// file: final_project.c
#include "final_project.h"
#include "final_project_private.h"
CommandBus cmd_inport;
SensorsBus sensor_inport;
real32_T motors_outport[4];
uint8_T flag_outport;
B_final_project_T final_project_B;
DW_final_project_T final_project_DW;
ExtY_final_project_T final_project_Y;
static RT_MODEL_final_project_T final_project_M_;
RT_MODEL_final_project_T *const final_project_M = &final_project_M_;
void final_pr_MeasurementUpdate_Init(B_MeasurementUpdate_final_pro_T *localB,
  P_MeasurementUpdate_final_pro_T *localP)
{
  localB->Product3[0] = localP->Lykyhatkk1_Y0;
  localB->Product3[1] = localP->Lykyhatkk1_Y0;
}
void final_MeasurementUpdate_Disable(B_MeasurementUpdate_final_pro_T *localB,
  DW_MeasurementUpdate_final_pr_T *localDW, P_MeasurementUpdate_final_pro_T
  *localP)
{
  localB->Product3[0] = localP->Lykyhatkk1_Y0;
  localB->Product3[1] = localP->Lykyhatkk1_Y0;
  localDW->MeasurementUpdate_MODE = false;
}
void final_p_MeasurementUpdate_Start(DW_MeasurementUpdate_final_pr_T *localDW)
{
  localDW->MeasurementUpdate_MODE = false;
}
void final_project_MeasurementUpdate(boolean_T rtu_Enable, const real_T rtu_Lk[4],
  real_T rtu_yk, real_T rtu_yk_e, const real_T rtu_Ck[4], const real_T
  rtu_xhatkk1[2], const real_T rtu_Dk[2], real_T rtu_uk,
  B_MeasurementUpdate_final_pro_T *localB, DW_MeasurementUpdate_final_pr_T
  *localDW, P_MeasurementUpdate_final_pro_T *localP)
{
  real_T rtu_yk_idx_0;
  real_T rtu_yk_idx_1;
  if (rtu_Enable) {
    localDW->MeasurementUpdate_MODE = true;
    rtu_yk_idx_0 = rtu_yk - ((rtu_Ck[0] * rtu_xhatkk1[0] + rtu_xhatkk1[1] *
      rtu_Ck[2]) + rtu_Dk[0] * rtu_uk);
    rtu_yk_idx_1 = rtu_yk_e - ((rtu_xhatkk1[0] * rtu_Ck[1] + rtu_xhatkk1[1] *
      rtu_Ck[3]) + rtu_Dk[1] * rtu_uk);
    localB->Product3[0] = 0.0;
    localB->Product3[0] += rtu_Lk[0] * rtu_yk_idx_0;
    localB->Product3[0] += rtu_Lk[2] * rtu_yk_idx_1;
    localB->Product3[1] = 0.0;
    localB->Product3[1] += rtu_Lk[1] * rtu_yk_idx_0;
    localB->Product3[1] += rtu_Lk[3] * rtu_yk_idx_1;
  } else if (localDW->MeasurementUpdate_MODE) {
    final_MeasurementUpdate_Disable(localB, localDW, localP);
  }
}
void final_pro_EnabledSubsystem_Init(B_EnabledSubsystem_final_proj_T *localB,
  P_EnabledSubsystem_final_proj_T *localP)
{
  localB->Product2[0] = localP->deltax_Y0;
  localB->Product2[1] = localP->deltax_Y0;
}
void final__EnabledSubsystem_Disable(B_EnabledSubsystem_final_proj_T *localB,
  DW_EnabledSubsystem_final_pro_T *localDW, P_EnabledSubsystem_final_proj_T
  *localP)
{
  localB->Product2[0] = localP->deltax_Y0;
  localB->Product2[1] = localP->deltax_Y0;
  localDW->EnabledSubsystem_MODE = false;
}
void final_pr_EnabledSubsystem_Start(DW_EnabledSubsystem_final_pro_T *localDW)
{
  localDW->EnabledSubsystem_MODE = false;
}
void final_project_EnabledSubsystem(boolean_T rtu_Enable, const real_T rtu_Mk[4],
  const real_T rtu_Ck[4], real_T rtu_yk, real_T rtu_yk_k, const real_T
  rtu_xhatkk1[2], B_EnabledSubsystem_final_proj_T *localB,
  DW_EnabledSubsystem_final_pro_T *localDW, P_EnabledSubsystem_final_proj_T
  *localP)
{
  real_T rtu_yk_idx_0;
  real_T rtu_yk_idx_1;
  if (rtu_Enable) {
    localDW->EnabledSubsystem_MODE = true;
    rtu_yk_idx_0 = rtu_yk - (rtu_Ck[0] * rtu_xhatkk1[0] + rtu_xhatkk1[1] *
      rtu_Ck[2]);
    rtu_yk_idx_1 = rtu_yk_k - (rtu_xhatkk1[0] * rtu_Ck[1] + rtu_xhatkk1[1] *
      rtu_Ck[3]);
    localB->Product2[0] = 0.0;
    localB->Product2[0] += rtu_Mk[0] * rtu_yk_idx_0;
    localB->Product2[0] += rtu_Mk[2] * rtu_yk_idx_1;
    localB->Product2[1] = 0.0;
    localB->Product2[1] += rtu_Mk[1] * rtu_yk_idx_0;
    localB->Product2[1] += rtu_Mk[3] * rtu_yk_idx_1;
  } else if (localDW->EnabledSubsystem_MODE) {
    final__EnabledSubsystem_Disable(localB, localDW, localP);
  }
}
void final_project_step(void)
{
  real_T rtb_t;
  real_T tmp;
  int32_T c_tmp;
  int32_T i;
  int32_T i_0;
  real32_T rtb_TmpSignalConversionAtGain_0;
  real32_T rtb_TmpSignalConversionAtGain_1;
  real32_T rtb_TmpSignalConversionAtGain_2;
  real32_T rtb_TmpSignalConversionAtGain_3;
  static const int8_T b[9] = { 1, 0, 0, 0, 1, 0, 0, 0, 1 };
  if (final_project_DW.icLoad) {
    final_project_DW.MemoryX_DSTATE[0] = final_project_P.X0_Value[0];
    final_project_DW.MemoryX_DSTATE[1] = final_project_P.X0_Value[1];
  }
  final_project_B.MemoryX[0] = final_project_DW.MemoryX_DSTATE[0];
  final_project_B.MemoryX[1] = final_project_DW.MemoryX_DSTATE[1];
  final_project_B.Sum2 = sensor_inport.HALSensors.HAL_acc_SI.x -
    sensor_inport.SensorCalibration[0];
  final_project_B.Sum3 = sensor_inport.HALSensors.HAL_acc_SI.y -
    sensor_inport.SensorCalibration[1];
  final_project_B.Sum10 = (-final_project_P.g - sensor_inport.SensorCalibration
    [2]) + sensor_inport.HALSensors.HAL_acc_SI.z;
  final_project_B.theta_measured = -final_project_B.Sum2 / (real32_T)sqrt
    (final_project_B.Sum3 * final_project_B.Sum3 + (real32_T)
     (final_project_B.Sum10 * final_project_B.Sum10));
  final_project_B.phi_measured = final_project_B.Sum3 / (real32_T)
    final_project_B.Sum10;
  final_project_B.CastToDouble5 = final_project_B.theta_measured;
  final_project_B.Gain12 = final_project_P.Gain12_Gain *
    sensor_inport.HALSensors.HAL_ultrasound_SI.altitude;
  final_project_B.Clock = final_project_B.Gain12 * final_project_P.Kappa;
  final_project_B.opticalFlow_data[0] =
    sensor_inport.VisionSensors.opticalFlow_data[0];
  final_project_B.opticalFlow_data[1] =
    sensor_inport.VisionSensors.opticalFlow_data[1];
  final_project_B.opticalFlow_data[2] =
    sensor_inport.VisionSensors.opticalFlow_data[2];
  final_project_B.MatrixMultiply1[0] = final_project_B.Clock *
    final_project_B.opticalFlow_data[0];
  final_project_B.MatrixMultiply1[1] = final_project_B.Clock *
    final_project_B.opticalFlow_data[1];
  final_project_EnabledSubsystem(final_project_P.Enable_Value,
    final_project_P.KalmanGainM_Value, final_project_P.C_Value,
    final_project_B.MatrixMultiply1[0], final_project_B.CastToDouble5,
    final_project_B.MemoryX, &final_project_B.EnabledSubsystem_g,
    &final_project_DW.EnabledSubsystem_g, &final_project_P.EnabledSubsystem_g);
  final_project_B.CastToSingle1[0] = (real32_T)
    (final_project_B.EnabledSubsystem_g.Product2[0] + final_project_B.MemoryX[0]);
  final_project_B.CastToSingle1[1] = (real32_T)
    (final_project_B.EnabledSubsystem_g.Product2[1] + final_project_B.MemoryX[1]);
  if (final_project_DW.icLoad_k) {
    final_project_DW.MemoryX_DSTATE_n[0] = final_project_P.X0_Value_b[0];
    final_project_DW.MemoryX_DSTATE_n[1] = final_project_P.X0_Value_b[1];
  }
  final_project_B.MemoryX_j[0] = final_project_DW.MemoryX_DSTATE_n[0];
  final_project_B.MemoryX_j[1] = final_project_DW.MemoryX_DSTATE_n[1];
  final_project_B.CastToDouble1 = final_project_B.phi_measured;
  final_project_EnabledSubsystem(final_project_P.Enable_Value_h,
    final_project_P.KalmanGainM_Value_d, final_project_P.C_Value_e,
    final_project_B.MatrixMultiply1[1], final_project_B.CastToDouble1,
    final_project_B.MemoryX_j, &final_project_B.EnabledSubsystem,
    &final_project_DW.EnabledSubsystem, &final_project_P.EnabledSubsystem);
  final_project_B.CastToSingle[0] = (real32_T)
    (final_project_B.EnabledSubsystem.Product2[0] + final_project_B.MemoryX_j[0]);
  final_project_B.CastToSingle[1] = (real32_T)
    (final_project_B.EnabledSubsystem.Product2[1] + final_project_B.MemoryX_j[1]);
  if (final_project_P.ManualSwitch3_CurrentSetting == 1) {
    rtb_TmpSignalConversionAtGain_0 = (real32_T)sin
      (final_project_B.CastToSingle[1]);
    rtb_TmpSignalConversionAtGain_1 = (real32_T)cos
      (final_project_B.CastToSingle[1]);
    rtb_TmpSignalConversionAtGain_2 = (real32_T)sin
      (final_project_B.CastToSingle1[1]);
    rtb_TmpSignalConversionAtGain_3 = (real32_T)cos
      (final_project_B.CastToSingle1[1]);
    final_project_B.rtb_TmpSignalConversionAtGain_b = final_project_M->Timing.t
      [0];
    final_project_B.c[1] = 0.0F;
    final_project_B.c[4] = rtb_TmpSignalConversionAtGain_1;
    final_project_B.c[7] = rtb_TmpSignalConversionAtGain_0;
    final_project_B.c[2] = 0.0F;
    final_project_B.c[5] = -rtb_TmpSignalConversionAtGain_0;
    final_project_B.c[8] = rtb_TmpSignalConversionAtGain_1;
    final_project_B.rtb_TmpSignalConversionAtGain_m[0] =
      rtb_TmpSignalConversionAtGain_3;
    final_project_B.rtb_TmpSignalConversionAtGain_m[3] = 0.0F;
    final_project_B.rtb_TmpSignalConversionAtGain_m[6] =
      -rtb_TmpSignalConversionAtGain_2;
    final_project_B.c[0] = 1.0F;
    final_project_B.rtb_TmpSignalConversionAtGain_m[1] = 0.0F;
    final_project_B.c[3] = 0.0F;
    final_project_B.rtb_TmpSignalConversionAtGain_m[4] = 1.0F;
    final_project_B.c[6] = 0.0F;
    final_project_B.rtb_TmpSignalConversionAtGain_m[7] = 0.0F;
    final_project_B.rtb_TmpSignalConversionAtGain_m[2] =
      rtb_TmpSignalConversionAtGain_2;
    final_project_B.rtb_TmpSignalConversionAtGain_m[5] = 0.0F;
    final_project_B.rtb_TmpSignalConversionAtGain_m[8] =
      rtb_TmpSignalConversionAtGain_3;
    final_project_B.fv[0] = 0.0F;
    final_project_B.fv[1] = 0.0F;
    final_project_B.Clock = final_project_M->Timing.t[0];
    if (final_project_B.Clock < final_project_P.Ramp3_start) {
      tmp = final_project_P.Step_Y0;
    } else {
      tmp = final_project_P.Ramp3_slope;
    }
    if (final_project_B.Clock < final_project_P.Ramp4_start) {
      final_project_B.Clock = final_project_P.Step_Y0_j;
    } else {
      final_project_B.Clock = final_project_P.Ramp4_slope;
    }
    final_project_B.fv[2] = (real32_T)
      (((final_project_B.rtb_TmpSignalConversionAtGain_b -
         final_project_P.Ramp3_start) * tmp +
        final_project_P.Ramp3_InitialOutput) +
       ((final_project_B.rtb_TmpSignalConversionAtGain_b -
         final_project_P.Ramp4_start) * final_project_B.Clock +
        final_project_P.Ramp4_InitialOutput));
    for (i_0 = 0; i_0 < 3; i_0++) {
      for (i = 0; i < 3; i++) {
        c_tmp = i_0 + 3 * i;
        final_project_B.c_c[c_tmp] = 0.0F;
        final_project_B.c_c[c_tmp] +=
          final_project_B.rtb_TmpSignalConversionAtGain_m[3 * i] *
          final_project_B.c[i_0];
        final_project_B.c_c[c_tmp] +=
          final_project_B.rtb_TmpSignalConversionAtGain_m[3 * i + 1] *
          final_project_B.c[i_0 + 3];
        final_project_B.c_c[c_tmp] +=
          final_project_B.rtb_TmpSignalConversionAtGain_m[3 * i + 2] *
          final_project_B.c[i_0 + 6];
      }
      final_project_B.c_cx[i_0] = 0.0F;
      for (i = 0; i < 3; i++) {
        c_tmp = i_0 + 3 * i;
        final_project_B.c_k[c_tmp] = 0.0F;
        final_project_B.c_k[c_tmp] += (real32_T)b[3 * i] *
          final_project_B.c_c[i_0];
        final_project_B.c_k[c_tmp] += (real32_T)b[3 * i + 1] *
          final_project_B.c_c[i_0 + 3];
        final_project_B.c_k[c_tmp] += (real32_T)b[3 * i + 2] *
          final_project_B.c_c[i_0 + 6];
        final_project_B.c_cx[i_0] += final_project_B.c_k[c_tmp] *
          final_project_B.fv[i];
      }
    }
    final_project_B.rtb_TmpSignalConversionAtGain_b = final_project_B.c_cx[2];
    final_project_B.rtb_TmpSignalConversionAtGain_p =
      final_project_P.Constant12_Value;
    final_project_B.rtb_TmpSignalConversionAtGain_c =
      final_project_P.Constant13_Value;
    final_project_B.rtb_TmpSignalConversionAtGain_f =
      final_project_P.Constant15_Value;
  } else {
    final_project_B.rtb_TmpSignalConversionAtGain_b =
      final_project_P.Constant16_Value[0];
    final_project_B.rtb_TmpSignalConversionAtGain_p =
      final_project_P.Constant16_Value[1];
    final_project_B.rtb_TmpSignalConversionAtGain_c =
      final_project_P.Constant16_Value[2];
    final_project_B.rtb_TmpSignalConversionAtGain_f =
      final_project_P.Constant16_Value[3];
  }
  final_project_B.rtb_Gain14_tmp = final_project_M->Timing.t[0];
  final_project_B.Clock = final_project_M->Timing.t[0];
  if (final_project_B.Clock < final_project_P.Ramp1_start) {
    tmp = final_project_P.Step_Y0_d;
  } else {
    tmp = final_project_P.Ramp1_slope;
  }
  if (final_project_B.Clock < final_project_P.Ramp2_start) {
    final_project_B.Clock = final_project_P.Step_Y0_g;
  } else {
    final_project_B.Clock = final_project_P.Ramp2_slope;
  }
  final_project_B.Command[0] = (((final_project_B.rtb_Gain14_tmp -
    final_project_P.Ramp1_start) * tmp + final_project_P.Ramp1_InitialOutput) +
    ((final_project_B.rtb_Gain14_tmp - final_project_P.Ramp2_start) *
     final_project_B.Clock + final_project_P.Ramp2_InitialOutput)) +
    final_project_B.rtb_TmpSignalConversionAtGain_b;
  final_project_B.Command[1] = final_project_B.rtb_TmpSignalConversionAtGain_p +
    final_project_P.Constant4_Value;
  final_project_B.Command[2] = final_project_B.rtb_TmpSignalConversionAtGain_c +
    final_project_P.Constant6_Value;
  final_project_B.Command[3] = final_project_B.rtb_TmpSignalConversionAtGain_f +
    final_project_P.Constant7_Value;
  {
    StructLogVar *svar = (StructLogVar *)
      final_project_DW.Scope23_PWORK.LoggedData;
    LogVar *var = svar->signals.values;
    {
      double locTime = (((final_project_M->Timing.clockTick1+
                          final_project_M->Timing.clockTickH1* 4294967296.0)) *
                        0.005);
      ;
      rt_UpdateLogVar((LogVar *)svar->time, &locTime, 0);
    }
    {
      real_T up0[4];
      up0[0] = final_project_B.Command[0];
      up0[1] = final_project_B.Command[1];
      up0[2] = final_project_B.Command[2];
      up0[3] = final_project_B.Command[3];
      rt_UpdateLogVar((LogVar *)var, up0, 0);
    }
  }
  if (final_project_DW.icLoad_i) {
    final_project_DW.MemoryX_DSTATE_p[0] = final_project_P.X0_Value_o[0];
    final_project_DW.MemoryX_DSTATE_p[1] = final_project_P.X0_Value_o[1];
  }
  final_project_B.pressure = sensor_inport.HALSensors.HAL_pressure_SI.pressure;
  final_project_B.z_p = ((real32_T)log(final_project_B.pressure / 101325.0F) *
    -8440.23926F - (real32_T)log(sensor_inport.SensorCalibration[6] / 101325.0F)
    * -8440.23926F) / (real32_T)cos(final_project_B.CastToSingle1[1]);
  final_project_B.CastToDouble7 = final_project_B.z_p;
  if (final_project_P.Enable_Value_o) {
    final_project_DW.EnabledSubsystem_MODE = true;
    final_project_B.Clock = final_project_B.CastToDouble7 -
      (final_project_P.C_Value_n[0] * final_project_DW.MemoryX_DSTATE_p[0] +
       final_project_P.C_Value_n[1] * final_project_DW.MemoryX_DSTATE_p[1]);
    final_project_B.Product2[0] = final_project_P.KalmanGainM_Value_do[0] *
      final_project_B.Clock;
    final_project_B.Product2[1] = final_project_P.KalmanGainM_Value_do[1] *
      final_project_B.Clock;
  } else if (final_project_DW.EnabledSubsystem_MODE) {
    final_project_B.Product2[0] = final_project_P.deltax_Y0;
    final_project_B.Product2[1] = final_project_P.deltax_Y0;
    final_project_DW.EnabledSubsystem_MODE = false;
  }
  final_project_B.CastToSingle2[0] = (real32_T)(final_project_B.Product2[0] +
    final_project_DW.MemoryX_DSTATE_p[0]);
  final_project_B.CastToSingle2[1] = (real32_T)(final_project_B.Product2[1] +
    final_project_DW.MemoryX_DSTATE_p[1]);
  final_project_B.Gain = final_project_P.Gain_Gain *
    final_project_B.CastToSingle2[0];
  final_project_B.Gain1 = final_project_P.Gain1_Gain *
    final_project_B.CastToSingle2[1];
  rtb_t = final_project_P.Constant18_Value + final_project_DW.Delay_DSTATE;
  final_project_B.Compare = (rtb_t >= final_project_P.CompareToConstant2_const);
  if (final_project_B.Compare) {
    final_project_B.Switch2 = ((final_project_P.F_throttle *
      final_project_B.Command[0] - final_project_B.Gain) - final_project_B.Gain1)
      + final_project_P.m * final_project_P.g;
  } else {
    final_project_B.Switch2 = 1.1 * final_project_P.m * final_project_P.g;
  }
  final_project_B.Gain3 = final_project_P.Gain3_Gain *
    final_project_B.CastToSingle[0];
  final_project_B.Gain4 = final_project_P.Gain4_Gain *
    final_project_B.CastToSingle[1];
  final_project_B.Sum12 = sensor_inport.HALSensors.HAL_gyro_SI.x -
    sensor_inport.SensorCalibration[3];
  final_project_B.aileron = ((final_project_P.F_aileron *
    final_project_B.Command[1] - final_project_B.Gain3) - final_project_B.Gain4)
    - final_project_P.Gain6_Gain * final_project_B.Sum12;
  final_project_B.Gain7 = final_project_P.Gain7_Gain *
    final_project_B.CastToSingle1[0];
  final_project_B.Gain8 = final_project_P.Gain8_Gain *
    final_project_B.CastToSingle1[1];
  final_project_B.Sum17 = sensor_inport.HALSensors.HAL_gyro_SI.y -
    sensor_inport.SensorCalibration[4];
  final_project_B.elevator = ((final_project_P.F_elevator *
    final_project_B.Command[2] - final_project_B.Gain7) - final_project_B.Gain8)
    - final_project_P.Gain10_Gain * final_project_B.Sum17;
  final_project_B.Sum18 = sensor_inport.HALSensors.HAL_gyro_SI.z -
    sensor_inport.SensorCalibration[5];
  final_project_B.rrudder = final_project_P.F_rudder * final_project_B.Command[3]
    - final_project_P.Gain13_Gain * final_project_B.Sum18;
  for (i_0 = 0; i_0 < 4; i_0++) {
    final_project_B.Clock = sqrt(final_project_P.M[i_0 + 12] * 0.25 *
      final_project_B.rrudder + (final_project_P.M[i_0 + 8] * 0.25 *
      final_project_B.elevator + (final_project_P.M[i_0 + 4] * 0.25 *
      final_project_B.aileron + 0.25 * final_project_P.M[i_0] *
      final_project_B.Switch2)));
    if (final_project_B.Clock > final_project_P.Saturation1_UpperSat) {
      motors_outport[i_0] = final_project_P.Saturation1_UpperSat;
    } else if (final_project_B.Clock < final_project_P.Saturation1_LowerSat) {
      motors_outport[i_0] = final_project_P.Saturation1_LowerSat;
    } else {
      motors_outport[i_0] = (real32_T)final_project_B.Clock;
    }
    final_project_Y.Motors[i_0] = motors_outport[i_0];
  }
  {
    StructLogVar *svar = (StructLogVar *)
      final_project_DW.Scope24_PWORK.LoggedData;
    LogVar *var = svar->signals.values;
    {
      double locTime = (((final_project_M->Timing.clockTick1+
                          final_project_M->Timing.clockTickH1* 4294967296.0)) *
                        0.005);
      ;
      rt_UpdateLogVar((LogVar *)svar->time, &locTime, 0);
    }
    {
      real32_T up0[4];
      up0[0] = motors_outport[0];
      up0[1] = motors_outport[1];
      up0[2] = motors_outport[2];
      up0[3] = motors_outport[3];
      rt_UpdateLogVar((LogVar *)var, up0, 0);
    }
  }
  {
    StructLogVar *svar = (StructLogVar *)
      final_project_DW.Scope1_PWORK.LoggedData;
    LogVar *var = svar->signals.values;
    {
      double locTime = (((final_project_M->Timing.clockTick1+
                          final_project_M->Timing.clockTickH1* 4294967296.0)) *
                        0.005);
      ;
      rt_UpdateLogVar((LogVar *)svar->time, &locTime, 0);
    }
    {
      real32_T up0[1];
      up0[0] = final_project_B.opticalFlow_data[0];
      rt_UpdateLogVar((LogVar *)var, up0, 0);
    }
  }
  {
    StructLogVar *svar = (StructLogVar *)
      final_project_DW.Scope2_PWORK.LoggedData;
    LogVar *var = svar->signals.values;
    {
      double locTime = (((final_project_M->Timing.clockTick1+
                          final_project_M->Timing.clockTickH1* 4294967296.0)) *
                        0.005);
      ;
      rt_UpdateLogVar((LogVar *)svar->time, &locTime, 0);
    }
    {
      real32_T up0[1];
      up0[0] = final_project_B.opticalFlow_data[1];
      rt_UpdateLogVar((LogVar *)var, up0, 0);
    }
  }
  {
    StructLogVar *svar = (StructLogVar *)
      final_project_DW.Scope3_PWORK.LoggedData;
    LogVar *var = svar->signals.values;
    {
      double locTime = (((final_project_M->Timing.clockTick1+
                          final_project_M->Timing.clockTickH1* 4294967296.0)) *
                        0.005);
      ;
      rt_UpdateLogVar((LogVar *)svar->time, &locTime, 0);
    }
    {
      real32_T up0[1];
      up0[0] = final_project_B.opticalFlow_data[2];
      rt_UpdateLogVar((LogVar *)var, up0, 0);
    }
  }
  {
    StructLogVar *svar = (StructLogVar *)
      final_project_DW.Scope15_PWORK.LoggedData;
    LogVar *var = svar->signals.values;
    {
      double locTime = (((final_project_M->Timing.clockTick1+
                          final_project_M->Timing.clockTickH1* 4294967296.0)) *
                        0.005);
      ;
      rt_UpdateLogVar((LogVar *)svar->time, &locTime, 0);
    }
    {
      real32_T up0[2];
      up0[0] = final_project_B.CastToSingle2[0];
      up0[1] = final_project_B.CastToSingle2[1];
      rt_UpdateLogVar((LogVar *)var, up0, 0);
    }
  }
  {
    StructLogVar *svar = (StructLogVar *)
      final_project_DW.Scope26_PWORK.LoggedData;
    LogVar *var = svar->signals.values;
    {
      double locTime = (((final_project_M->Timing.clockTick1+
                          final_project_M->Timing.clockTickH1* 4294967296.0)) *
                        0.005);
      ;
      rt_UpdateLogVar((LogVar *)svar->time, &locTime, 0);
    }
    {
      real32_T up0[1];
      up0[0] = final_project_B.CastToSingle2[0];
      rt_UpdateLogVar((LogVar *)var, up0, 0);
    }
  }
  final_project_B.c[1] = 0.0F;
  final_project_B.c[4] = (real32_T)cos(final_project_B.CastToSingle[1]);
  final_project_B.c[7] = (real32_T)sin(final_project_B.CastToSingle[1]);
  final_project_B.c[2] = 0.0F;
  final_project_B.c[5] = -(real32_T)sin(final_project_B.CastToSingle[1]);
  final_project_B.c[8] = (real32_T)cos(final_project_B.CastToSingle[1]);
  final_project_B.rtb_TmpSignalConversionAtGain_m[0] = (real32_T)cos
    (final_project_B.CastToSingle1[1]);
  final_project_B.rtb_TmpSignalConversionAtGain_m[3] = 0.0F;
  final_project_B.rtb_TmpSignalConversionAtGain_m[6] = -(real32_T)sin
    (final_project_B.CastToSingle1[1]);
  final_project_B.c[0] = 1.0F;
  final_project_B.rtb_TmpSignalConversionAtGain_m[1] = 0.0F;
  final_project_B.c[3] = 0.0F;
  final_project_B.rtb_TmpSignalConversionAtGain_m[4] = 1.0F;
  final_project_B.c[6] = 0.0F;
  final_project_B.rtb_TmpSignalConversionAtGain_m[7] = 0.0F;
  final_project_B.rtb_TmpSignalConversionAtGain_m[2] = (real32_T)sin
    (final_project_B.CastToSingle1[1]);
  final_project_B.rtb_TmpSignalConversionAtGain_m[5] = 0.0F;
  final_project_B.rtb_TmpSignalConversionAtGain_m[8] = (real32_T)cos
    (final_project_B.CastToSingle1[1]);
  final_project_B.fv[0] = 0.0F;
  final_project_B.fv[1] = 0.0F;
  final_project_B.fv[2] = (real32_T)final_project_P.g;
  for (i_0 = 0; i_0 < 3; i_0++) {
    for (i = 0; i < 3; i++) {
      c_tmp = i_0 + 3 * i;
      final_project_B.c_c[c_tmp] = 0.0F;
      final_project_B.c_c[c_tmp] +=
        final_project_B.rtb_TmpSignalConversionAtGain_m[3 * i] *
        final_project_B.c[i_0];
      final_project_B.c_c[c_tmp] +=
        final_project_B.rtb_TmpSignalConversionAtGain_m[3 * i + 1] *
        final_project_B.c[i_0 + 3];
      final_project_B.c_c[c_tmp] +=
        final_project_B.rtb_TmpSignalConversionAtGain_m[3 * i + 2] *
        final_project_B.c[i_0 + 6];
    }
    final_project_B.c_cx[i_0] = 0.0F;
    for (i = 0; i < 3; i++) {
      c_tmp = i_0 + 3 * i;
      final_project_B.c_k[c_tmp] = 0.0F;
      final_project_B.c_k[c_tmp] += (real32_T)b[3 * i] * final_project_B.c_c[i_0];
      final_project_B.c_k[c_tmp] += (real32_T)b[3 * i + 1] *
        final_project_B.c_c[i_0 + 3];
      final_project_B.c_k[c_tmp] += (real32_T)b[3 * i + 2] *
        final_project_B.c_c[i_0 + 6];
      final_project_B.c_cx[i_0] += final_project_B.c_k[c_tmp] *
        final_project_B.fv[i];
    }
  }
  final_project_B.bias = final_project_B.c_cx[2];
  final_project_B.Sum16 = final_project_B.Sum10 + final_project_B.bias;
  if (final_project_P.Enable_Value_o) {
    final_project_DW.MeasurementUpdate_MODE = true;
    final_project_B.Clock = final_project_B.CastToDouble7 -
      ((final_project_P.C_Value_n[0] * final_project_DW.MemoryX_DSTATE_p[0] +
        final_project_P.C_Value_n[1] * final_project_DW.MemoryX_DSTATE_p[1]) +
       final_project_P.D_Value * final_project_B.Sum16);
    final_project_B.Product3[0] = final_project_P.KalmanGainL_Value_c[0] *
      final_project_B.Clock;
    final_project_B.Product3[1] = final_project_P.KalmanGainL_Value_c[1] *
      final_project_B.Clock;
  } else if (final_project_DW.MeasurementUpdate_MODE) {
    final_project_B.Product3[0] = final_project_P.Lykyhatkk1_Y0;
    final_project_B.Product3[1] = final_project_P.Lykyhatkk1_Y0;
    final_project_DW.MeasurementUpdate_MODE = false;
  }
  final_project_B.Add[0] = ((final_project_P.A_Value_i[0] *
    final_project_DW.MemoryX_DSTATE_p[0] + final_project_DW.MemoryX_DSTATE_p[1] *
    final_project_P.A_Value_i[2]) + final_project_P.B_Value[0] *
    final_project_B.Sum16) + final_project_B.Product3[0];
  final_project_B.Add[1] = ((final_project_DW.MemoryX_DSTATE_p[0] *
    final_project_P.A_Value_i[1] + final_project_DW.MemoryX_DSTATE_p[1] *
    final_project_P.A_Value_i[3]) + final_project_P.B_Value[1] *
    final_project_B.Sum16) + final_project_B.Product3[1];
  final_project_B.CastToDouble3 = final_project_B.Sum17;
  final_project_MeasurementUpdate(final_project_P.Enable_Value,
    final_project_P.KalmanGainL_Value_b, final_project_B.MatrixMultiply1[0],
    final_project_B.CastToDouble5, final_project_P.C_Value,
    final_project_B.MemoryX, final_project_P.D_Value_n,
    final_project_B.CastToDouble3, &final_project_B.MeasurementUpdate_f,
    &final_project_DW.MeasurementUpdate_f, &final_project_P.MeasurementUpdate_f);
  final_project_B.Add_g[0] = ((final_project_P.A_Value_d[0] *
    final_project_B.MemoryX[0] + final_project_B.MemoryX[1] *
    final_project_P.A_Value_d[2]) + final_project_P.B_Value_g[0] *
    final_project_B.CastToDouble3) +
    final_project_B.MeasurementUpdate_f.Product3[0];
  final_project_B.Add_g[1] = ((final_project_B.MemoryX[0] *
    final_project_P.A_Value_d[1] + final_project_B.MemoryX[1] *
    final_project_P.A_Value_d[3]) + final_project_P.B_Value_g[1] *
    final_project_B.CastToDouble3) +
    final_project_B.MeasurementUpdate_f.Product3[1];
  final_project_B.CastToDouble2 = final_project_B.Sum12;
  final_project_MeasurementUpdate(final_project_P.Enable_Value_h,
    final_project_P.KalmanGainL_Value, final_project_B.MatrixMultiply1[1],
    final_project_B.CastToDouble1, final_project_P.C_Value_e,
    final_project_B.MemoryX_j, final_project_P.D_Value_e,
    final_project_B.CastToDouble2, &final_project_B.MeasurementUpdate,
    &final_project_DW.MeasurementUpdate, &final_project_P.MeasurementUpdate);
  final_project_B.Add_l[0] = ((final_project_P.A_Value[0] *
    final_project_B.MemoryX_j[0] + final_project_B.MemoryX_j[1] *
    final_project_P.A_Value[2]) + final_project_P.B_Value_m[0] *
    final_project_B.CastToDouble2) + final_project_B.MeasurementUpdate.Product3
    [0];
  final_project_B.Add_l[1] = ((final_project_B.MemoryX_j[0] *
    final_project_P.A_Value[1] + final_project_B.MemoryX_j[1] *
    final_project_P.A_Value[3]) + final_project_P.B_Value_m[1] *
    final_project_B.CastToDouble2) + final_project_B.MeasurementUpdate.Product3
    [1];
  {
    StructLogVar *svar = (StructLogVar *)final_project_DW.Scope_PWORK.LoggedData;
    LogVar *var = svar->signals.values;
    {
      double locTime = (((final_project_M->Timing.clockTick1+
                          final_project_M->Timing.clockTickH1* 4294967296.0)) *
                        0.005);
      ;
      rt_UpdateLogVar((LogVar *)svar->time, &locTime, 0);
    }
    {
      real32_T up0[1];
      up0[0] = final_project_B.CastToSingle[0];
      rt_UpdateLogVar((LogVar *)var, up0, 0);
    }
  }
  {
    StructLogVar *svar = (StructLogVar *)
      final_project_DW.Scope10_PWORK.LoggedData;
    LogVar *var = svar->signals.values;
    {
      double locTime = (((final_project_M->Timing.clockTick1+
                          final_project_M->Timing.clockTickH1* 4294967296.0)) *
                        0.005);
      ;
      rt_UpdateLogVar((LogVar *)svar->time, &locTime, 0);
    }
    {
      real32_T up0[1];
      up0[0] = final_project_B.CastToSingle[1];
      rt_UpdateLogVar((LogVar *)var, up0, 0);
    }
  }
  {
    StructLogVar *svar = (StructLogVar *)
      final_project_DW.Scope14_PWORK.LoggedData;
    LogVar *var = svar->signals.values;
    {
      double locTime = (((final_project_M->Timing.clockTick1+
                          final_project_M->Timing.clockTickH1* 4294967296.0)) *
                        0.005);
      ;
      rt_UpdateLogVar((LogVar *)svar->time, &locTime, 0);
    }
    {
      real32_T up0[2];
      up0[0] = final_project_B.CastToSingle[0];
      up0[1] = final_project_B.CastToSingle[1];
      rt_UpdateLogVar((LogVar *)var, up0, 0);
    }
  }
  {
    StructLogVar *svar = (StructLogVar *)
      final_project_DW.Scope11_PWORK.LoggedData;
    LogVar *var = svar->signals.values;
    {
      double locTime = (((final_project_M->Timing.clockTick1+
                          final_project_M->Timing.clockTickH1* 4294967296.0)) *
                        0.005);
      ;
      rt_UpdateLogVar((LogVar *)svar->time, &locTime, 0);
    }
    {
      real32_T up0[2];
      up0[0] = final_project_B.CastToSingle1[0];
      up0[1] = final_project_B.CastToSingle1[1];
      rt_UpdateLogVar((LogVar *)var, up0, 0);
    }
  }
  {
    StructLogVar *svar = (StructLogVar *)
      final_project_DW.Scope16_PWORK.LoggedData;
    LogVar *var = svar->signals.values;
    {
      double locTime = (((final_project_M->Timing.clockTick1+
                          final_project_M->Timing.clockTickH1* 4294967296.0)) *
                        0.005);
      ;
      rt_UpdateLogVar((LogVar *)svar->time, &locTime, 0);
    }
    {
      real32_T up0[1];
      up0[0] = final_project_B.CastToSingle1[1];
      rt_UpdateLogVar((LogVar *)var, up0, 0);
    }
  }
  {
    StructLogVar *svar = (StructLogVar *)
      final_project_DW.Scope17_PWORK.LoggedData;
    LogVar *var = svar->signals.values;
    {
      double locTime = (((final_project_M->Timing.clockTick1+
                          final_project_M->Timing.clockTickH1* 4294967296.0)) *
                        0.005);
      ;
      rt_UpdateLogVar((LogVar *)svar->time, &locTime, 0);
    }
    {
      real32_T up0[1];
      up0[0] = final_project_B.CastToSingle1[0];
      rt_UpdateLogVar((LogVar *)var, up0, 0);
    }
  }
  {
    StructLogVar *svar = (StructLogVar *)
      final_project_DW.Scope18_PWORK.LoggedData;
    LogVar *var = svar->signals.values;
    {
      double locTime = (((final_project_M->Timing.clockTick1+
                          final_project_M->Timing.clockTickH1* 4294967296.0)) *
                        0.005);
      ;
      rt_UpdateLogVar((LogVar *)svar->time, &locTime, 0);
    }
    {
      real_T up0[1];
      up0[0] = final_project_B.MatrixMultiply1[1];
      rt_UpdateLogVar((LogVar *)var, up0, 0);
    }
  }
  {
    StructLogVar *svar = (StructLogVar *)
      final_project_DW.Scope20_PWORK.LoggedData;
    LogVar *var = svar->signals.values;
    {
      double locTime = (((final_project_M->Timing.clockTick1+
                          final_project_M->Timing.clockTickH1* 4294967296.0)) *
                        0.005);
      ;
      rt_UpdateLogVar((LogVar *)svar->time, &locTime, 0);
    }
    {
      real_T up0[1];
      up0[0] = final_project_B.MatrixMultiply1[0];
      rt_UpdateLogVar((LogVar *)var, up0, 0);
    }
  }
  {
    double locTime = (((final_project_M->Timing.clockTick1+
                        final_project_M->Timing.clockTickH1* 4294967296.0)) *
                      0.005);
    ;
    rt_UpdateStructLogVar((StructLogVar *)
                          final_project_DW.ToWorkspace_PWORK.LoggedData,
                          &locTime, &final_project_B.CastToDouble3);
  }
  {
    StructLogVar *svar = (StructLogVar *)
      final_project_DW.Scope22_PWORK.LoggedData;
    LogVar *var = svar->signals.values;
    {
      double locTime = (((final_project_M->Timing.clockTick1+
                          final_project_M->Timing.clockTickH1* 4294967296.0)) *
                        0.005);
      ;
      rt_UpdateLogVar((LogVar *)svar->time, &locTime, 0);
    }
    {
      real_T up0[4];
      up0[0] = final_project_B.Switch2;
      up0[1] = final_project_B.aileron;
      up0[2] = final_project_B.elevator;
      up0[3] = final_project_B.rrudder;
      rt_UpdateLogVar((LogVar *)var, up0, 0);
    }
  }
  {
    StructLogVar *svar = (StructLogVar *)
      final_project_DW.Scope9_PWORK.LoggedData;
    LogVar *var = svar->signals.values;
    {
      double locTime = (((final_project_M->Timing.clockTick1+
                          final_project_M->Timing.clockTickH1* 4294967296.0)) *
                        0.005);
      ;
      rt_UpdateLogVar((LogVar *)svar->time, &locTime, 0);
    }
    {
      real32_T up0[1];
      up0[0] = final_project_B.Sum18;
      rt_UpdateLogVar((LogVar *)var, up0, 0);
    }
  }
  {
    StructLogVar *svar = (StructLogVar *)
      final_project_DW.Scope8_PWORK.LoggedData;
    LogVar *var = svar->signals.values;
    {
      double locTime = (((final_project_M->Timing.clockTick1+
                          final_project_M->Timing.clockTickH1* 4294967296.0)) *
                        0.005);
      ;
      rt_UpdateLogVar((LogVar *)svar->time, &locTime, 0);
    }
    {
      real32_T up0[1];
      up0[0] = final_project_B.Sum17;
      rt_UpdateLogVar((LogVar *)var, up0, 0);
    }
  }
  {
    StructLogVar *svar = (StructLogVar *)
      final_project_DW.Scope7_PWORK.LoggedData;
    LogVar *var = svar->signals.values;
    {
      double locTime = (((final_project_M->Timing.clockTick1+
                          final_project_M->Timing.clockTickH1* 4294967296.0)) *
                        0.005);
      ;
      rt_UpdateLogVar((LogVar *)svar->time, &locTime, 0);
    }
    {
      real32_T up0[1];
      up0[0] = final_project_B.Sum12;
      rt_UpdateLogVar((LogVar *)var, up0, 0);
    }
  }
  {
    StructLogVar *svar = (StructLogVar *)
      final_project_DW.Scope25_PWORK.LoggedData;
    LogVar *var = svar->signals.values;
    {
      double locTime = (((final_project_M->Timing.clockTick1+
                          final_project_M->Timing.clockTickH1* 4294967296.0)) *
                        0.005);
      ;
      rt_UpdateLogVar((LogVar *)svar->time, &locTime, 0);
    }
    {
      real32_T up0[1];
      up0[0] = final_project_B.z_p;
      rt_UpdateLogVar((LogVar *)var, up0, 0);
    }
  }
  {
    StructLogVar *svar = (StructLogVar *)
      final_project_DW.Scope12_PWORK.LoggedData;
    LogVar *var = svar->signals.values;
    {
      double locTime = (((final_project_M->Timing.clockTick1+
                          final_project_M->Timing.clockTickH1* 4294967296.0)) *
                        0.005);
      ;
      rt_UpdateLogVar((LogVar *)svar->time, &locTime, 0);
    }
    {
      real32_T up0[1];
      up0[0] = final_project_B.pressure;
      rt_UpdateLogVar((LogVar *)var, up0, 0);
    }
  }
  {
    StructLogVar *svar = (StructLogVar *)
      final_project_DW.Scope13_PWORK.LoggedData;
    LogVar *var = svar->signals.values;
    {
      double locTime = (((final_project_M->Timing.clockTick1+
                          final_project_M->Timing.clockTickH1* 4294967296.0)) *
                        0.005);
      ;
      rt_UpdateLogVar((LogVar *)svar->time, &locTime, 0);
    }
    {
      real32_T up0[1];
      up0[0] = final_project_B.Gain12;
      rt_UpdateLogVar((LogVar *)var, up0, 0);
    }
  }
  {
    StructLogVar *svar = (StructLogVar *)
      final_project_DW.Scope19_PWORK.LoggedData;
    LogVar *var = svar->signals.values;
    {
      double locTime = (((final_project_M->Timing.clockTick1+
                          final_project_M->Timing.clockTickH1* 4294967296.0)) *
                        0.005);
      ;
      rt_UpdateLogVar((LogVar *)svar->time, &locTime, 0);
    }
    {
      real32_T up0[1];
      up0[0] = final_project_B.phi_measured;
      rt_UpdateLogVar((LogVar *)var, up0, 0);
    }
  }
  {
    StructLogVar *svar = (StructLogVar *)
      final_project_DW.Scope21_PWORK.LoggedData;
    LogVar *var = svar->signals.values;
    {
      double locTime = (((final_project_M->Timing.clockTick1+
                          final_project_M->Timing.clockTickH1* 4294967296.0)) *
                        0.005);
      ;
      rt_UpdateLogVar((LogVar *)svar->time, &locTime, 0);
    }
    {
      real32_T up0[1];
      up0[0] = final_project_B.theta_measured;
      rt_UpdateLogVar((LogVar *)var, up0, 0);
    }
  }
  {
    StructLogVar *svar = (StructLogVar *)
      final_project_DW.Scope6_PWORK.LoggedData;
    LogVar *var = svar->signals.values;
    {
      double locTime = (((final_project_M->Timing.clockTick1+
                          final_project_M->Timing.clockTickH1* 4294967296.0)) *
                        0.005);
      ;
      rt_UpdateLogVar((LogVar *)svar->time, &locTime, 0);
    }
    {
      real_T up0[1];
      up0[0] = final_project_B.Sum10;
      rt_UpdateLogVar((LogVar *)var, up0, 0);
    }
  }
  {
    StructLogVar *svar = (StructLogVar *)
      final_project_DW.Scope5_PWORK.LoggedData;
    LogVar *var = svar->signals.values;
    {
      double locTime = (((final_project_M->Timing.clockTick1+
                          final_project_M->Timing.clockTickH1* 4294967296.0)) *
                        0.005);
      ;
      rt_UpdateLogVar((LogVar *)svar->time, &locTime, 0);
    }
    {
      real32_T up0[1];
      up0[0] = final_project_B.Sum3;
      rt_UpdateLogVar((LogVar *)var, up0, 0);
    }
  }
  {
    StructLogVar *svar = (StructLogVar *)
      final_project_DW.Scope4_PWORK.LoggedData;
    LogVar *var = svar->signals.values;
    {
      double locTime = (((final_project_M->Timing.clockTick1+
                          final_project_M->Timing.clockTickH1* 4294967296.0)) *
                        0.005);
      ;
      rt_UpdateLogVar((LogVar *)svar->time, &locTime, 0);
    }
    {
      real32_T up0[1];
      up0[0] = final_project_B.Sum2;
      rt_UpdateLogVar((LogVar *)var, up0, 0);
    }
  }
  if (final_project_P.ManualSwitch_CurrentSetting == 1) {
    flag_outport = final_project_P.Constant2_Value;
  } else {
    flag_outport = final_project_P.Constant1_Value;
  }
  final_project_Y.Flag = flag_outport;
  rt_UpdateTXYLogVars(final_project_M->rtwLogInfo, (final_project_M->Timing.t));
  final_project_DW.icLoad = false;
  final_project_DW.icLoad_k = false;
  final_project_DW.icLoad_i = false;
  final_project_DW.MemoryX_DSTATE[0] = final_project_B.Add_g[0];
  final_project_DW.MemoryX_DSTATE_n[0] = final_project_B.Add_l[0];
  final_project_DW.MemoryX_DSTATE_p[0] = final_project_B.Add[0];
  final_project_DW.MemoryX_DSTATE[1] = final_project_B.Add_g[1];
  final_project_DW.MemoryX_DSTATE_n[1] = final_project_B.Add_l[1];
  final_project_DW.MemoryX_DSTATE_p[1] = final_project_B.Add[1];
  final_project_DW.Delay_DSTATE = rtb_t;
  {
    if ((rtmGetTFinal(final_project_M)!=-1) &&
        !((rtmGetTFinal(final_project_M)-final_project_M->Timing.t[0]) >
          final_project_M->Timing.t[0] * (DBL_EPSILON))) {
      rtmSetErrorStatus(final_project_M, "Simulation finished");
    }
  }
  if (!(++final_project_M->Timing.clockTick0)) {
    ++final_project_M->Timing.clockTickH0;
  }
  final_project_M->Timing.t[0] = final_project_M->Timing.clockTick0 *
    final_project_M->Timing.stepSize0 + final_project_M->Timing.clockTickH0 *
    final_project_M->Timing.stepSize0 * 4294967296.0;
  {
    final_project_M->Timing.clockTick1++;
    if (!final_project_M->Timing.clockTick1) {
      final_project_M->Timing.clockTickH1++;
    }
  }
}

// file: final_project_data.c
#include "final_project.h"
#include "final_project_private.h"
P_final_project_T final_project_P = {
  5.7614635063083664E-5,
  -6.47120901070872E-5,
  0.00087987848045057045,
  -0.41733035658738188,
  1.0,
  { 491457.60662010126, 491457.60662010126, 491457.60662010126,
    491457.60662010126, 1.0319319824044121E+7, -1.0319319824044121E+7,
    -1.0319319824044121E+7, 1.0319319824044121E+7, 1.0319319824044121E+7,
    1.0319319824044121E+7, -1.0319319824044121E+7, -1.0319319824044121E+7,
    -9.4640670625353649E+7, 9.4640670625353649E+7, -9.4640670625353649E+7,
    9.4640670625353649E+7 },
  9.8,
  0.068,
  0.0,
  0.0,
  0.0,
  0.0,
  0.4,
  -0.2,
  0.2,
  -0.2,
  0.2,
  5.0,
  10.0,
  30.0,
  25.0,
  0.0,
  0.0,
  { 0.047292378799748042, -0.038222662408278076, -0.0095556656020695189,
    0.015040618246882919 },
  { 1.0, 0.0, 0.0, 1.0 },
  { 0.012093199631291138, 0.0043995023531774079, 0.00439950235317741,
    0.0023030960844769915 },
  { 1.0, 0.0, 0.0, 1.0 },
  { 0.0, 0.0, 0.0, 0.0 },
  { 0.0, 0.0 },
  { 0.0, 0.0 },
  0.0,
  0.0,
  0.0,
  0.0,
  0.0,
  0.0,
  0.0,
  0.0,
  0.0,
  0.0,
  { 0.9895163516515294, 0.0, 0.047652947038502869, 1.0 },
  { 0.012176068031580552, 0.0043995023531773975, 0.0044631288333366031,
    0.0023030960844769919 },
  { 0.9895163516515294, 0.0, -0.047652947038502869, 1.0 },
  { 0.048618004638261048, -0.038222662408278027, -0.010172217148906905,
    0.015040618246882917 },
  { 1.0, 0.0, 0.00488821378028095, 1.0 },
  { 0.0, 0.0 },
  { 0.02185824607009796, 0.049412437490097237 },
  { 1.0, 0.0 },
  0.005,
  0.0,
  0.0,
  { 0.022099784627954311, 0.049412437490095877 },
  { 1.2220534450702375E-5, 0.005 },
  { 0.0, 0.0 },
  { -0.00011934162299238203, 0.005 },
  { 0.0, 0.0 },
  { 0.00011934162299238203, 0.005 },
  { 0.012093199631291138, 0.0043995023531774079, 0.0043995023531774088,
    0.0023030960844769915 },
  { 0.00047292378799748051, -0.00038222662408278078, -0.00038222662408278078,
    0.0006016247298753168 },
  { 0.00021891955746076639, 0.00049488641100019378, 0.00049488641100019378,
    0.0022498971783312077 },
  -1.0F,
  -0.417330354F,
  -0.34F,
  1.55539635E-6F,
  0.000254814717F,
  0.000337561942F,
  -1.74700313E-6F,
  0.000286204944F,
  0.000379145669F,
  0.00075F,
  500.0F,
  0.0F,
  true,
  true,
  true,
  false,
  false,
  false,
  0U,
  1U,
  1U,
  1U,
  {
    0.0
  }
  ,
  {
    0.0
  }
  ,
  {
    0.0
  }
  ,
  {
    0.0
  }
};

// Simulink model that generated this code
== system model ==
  Inport#1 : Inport
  Inport#2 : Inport
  Motors : Outport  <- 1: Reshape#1
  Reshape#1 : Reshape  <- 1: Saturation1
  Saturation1 : Saturate  UpperLimit=500  LowerLimit=0  <- 1: Sqrt#1
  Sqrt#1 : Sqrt  <- 1: Gain#1
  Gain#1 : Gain  Gain=1/4*M  Multiplication=Matrix(K*u)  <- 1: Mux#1
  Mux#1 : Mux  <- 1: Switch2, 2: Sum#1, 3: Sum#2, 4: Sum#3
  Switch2 : Switch  Criteria=u2 > Threshold  <- 1: Sum#4, 2: CompareToConstant2, 3: Constant#1
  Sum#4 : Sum  Inputs=++  <- 1: Sum#5, 2: Constant#2
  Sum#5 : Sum  Inputs=+-  <- 1: Sum#6, 2: Gain1
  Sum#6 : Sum  Inputs=+-  <- 1: Gain#2, 2: Gain
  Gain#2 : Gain  Gain=F_throttle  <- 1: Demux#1
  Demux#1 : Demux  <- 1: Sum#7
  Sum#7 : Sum  Inputs=++  <- 1: ManualSwitch3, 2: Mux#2
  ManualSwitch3 : ManualSwitch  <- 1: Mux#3, 2: Constant16
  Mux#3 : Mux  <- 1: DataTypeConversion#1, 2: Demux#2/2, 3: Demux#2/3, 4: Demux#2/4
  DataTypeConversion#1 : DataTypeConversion  <- 1: MATLABFunction#1
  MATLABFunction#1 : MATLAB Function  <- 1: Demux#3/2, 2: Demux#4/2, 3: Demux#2
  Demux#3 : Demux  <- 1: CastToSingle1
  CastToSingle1 : DataTypeConversion  <- 1: KalmanFilter#1
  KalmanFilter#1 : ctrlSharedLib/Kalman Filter  TimeDomain=Discrete-Time  A=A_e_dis  B=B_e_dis  C=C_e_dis  D=0  X0=0  N=0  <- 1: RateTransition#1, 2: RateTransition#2
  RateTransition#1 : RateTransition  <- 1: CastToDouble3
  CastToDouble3 : DataTypeConversion  <- 1: Sum17
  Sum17 : Sum  Inputs=+-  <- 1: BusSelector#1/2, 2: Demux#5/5
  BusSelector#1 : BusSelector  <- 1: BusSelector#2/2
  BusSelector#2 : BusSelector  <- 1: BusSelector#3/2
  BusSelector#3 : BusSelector  <- 1: Inport#2
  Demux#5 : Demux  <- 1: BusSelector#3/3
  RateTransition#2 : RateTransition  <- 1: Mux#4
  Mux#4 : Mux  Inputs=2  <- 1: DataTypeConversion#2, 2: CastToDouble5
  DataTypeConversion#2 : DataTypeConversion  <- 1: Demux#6
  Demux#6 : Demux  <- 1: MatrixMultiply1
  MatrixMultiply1 : Product  <- 1: Product#1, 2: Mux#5
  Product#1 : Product  <- 1: Gain12, 2: Constant#3
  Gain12 : Gain  Gain=-1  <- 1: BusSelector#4
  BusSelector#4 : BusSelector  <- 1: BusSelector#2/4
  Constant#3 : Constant  Value=Kappa
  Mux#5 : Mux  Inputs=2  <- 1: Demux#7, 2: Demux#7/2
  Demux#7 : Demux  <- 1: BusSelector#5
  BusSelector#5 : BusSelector  <- 1: BusSelector#3
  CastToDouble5 : DataTypeConversion  <- 1: MATLABFunction#2
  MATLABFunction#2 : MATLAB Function  <- 1: Sum2, 2: Sum3, 3: Sum10
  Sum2 : Sum  Inputs=+-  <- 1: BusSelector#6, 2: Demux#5
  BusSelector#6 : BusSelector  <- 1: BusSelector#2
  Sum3 : Sum  Inputs=+-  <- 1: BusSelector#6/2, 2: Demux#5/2
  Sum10 : Sum  Inputs=++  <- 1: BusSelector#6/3, 2: Sum#8
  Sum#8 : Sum  Inputs=+-  <- 1: Constant#4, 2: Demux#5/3
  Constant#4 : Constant  Value=-g
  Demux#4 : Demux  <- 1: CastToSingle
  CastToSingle : DataTypeConversion  <- 1: KalmanFilter#2
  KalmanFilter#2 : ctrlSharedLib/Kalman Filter  TimeDomain=Discrete-Time  A=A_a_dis  B=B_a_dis  C=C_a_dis  D=0  X0=0  N=0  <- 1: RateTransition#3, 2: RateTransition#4
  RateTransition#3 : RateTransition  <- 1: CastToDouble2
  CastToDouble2 : DataTypeConversion  <- 1: Sum12
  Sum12 : Sum  Inputs=+-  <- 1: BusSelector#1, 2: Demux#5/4
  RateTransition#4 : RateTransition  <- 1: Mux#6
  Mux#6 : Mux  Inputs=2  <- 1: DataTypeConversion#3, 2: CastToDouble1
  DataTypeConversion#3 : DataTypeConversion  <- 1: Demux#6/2
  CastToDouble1 : DataTypeConversion  <- 1: MATLABFunction#2/2
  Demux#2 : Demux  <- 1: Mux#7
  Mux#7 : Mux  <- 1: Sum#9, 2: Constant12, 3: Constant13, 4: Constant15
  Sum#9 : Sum  Inputs=++  <- 1: Ramp3, 2: Ramp4
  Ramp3 : simulink/Sources/Ramp  slope=-.2  InitialOutput=0
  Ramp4 : simulink/Sources/Ramp  slope=.2  InitialOutput=0
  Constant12 : Constant  Value=0
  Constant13 : Constant  Value=0
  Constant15 : Constant  Value=0
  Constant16 : Constant  Value=[0; 0; 0; 0]
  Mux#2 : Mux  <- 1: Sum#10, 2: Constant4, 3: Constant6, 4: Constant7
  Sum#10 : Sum  Inputs=++  <- 1: Ramp1, 2: Ramp2
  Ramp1 : simulink/Sources/Ramp  slope=-.2  InitialOutput=0
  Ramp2 : simulink/Sources/Ramp  slope=.2  InitialOutput=0
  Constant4 : Constant  Value=0
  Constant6 : Constant  Value=0
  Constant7 : Constant  Value=0
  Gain : Gain  Gain=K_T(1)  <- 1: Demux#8
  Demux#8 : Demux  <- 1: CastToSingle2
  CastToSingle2 : DataTypeConversion  <- 1: KalmanFilter#3
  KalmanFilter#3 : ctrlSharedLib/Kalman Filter  TimeDomain=Discrete-Time  A=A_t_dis  B=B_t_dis  C=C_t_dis  D=0  X0=0  N=0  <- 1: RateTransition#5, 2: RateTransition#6
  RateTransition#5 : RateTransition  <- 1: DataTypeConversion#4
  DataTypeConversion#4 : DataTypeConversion  <- 1: Sum16
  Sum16 : Sum  Inputs=++  <- 1: Sum10, 2: MATLABFunction#3
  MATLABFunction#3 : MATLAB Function  <- 1: Constant#5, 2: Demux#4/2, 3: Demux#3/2
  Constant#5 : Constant  Value=g
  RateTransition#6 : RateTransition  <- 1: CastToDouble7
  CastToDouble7 : DataTypeConversion  <- 1: MATLABFunction#4
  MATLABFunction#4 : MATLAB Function  <- 1: BusSelector#7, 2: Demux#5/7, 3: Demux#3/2
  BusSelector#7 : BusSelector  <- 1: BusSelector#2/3
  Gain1 : Gain  Gain=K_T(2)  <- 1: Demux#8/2
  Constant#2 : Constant  Value=m*g
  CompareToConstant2 : simulink/Logic and Bit Operations/Compare To Constant  relop=>=  const=0.4  <- 1: Sum#11
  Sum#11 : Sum  Inputs=++  <- 1: Constant18, 2: Delay
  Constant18 : Constant  Value=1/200
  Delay : Delay  DelayLength=1  <- 1: Sum#11
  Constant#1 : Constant  Value=1.1*m*g
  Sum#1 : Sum  Inputs=+-  <- 1: Sum#12, 2: Gain6
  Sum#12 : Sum  Inputs=+-  <- 1: Sum#13, 2: Gain4
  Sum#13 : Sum  Inputs=+-  <- 1: Gain#3, 2: Gain3
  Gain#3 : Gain  Gain=F_aileron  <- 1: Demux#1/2
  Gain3 : Gain  Gain=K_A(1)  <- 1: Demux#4
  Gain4 : Gain  Gain=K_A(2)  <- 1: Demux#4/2
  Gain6 : Gain  Gain=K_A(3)  <- 1: Sum12
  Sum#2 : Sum  Inputs=+-  <- 1: Sum#14, 2: Gain10
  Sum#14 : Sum  Inputs=+-  <- 1: Sum#15, 2: Gain8
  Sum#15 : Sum  Inputs=+-  <- 1: Gain#4, 2: Gain7
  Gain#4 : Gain  Gain=F_elevator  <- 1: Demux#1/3
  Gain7 : Gain  Gain=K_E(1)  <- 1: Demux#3
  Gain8 : Gain  Gain=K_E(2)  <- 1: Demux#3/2
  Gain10 : Gain  Gain=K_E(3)  <- 1: Sum17
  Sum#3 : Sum  Inputs=+-  <- 1: Gain14, 2: Gain13
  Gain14 : Gain  Gain=F_rudder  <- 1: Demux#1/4
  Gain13 : Gain  Gain=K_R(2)  <- 1: Sum18
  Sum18 : Sum  Inputs=+-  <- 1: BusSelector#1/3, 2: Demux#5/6
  Flag : Outport  <- 1: ManualSwitch
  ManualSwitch : ManualSwitch  <- 1: Constant2, 2: Constant1
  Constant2 : Constant  Value=0
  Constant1 : Constant
== matlab function MATLABFunction#4 ==
function z_p = fcn(pressure,pres_0,theta_kf) 
g = 9.8; % acceleration due to gravity m/s^2
M = 0.0289644; % molar mass of air in kg/mol
R = 8.31432; % universal gas constant Nm/mol/k
p0 = 101325; % Pa standard pressure

T =288.15;  % Assumed temperature in kelvin
K =-g*M/R/T;
z_p = (1/K.*log(pressure./p0) - 1/K.*log(pres_0./p0))/cos(theta_kf);

== matlab function MATLABFunction#2 ==
function [theta_measured,phi_measured]= fcn(a_x,a_y,a_z)
theta_measured = -a_x / sqrt(a_y^2 + a_z^2);
phi_measured = a_y/a_z;

== matlab function MATLABFunction#1 ==
function Pbz_cmd = fcn(theta_kf,phi_kf,P_D_cmd)
    phi = phi_kf;
    theta = theta_kf;
    psi = 0;
    R_phi = [1 0 0;
             0 cos(phi) sin(phi);
             0 -sin(phi) cos(phi)];
    R_theta = [cos(theta) 0 -sin(theta);
               0 1 0;
               sin(theta) 0 cos(theta)];
    R_psi = [cos(psi) sin(psi) 0;
             -sin(psi) cos(psi) 0;
             0 0 1];
    R = R_phi*R_theta*R_psi;
    Pb = R*[0; 0; P_D_cmd];
    Pbz_cmd = Pb(3);

== matlab function MATLABFunction#3 ==
function bias = fcn(g,phi,theta)
psi = 0;
R_phi = [1 0 0;
         0 cos(phi) sin(phi);
         0 -sin(phi) cos(phi)];
R_theta = [cos(theta) 0 -sin(theta);
           0 1 0;
           sin(theta) 0 cos(theta)];
R_psi = [cos(psi) sin(psi) 0;
         -sin(psi) cos(psi) 0;
         0 0 1];
R = R_phi*R_theta*R_psi;
G_b = R*[0; 0; g];
bias = G_b(3);
